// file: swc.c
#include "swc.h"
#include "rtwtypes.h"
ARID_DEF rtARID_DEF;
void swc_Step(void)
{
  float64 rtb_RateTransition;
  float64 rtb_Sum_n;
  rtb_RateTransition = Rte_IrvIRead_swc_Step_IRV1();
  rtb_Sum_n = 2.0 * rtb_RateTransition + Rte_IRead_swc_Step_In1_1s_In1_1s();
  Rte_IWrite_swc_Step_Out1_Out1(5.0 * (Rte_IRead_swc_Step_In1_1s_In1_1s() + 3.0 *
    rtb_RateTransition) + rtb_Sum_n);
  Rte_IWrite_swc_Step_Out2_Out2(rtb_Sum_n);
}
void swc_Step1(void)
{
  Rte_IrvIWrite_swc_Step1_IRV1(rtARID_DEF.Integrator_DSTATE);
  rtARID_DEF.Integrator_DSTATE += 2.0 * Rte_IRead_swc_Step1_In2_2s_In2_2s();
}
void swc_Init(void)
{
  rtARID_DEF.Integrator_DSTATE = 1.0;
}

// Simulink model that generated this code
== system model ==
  In1_1s : Inport
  In2_2s : Inport
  Out1 : Outport  <- 1: Sum
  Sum : Sum  Inputs=++  <- 1: Subsystem#1, 2: Subsystem#2
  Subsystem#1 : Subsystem  <- 1: In1_1s, 2: RateTransition
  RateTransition : RateTransition  <- 1: Integrator
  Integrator : DiscreteIntegrator  <- 1: In2_2s
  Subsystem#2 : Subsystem  <- 1: RateTransition, 2: In1_1s
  Out2 : Outport  <- 1: Subsystem#2
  Subsystem#3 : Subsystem
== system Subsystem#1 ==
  In1 : Inport
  In2 : Inport
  Outport#1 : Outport  <- 1: Gain#1
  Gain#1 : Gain  Gain=5  <- 1: Sum#1
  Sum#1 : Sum  Inputs=++  <- 1: In1, 2: Gain#2
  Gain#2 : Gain  Gain=3  <- 1: In2
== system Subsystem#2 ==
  Inport#1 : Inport
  Inport#2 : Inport
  Outport#2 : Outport  <- 1: Sum#2
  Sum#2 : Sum  Inputs=++  <- 1: Gain#3, 2: Inport#2
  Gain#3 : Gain  Gain=2  <- 1: Inport#1
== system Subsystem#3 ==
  StateWriter#1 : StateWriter  <- 1: Constant#1
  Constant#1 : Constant
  EventListener#1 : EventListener
